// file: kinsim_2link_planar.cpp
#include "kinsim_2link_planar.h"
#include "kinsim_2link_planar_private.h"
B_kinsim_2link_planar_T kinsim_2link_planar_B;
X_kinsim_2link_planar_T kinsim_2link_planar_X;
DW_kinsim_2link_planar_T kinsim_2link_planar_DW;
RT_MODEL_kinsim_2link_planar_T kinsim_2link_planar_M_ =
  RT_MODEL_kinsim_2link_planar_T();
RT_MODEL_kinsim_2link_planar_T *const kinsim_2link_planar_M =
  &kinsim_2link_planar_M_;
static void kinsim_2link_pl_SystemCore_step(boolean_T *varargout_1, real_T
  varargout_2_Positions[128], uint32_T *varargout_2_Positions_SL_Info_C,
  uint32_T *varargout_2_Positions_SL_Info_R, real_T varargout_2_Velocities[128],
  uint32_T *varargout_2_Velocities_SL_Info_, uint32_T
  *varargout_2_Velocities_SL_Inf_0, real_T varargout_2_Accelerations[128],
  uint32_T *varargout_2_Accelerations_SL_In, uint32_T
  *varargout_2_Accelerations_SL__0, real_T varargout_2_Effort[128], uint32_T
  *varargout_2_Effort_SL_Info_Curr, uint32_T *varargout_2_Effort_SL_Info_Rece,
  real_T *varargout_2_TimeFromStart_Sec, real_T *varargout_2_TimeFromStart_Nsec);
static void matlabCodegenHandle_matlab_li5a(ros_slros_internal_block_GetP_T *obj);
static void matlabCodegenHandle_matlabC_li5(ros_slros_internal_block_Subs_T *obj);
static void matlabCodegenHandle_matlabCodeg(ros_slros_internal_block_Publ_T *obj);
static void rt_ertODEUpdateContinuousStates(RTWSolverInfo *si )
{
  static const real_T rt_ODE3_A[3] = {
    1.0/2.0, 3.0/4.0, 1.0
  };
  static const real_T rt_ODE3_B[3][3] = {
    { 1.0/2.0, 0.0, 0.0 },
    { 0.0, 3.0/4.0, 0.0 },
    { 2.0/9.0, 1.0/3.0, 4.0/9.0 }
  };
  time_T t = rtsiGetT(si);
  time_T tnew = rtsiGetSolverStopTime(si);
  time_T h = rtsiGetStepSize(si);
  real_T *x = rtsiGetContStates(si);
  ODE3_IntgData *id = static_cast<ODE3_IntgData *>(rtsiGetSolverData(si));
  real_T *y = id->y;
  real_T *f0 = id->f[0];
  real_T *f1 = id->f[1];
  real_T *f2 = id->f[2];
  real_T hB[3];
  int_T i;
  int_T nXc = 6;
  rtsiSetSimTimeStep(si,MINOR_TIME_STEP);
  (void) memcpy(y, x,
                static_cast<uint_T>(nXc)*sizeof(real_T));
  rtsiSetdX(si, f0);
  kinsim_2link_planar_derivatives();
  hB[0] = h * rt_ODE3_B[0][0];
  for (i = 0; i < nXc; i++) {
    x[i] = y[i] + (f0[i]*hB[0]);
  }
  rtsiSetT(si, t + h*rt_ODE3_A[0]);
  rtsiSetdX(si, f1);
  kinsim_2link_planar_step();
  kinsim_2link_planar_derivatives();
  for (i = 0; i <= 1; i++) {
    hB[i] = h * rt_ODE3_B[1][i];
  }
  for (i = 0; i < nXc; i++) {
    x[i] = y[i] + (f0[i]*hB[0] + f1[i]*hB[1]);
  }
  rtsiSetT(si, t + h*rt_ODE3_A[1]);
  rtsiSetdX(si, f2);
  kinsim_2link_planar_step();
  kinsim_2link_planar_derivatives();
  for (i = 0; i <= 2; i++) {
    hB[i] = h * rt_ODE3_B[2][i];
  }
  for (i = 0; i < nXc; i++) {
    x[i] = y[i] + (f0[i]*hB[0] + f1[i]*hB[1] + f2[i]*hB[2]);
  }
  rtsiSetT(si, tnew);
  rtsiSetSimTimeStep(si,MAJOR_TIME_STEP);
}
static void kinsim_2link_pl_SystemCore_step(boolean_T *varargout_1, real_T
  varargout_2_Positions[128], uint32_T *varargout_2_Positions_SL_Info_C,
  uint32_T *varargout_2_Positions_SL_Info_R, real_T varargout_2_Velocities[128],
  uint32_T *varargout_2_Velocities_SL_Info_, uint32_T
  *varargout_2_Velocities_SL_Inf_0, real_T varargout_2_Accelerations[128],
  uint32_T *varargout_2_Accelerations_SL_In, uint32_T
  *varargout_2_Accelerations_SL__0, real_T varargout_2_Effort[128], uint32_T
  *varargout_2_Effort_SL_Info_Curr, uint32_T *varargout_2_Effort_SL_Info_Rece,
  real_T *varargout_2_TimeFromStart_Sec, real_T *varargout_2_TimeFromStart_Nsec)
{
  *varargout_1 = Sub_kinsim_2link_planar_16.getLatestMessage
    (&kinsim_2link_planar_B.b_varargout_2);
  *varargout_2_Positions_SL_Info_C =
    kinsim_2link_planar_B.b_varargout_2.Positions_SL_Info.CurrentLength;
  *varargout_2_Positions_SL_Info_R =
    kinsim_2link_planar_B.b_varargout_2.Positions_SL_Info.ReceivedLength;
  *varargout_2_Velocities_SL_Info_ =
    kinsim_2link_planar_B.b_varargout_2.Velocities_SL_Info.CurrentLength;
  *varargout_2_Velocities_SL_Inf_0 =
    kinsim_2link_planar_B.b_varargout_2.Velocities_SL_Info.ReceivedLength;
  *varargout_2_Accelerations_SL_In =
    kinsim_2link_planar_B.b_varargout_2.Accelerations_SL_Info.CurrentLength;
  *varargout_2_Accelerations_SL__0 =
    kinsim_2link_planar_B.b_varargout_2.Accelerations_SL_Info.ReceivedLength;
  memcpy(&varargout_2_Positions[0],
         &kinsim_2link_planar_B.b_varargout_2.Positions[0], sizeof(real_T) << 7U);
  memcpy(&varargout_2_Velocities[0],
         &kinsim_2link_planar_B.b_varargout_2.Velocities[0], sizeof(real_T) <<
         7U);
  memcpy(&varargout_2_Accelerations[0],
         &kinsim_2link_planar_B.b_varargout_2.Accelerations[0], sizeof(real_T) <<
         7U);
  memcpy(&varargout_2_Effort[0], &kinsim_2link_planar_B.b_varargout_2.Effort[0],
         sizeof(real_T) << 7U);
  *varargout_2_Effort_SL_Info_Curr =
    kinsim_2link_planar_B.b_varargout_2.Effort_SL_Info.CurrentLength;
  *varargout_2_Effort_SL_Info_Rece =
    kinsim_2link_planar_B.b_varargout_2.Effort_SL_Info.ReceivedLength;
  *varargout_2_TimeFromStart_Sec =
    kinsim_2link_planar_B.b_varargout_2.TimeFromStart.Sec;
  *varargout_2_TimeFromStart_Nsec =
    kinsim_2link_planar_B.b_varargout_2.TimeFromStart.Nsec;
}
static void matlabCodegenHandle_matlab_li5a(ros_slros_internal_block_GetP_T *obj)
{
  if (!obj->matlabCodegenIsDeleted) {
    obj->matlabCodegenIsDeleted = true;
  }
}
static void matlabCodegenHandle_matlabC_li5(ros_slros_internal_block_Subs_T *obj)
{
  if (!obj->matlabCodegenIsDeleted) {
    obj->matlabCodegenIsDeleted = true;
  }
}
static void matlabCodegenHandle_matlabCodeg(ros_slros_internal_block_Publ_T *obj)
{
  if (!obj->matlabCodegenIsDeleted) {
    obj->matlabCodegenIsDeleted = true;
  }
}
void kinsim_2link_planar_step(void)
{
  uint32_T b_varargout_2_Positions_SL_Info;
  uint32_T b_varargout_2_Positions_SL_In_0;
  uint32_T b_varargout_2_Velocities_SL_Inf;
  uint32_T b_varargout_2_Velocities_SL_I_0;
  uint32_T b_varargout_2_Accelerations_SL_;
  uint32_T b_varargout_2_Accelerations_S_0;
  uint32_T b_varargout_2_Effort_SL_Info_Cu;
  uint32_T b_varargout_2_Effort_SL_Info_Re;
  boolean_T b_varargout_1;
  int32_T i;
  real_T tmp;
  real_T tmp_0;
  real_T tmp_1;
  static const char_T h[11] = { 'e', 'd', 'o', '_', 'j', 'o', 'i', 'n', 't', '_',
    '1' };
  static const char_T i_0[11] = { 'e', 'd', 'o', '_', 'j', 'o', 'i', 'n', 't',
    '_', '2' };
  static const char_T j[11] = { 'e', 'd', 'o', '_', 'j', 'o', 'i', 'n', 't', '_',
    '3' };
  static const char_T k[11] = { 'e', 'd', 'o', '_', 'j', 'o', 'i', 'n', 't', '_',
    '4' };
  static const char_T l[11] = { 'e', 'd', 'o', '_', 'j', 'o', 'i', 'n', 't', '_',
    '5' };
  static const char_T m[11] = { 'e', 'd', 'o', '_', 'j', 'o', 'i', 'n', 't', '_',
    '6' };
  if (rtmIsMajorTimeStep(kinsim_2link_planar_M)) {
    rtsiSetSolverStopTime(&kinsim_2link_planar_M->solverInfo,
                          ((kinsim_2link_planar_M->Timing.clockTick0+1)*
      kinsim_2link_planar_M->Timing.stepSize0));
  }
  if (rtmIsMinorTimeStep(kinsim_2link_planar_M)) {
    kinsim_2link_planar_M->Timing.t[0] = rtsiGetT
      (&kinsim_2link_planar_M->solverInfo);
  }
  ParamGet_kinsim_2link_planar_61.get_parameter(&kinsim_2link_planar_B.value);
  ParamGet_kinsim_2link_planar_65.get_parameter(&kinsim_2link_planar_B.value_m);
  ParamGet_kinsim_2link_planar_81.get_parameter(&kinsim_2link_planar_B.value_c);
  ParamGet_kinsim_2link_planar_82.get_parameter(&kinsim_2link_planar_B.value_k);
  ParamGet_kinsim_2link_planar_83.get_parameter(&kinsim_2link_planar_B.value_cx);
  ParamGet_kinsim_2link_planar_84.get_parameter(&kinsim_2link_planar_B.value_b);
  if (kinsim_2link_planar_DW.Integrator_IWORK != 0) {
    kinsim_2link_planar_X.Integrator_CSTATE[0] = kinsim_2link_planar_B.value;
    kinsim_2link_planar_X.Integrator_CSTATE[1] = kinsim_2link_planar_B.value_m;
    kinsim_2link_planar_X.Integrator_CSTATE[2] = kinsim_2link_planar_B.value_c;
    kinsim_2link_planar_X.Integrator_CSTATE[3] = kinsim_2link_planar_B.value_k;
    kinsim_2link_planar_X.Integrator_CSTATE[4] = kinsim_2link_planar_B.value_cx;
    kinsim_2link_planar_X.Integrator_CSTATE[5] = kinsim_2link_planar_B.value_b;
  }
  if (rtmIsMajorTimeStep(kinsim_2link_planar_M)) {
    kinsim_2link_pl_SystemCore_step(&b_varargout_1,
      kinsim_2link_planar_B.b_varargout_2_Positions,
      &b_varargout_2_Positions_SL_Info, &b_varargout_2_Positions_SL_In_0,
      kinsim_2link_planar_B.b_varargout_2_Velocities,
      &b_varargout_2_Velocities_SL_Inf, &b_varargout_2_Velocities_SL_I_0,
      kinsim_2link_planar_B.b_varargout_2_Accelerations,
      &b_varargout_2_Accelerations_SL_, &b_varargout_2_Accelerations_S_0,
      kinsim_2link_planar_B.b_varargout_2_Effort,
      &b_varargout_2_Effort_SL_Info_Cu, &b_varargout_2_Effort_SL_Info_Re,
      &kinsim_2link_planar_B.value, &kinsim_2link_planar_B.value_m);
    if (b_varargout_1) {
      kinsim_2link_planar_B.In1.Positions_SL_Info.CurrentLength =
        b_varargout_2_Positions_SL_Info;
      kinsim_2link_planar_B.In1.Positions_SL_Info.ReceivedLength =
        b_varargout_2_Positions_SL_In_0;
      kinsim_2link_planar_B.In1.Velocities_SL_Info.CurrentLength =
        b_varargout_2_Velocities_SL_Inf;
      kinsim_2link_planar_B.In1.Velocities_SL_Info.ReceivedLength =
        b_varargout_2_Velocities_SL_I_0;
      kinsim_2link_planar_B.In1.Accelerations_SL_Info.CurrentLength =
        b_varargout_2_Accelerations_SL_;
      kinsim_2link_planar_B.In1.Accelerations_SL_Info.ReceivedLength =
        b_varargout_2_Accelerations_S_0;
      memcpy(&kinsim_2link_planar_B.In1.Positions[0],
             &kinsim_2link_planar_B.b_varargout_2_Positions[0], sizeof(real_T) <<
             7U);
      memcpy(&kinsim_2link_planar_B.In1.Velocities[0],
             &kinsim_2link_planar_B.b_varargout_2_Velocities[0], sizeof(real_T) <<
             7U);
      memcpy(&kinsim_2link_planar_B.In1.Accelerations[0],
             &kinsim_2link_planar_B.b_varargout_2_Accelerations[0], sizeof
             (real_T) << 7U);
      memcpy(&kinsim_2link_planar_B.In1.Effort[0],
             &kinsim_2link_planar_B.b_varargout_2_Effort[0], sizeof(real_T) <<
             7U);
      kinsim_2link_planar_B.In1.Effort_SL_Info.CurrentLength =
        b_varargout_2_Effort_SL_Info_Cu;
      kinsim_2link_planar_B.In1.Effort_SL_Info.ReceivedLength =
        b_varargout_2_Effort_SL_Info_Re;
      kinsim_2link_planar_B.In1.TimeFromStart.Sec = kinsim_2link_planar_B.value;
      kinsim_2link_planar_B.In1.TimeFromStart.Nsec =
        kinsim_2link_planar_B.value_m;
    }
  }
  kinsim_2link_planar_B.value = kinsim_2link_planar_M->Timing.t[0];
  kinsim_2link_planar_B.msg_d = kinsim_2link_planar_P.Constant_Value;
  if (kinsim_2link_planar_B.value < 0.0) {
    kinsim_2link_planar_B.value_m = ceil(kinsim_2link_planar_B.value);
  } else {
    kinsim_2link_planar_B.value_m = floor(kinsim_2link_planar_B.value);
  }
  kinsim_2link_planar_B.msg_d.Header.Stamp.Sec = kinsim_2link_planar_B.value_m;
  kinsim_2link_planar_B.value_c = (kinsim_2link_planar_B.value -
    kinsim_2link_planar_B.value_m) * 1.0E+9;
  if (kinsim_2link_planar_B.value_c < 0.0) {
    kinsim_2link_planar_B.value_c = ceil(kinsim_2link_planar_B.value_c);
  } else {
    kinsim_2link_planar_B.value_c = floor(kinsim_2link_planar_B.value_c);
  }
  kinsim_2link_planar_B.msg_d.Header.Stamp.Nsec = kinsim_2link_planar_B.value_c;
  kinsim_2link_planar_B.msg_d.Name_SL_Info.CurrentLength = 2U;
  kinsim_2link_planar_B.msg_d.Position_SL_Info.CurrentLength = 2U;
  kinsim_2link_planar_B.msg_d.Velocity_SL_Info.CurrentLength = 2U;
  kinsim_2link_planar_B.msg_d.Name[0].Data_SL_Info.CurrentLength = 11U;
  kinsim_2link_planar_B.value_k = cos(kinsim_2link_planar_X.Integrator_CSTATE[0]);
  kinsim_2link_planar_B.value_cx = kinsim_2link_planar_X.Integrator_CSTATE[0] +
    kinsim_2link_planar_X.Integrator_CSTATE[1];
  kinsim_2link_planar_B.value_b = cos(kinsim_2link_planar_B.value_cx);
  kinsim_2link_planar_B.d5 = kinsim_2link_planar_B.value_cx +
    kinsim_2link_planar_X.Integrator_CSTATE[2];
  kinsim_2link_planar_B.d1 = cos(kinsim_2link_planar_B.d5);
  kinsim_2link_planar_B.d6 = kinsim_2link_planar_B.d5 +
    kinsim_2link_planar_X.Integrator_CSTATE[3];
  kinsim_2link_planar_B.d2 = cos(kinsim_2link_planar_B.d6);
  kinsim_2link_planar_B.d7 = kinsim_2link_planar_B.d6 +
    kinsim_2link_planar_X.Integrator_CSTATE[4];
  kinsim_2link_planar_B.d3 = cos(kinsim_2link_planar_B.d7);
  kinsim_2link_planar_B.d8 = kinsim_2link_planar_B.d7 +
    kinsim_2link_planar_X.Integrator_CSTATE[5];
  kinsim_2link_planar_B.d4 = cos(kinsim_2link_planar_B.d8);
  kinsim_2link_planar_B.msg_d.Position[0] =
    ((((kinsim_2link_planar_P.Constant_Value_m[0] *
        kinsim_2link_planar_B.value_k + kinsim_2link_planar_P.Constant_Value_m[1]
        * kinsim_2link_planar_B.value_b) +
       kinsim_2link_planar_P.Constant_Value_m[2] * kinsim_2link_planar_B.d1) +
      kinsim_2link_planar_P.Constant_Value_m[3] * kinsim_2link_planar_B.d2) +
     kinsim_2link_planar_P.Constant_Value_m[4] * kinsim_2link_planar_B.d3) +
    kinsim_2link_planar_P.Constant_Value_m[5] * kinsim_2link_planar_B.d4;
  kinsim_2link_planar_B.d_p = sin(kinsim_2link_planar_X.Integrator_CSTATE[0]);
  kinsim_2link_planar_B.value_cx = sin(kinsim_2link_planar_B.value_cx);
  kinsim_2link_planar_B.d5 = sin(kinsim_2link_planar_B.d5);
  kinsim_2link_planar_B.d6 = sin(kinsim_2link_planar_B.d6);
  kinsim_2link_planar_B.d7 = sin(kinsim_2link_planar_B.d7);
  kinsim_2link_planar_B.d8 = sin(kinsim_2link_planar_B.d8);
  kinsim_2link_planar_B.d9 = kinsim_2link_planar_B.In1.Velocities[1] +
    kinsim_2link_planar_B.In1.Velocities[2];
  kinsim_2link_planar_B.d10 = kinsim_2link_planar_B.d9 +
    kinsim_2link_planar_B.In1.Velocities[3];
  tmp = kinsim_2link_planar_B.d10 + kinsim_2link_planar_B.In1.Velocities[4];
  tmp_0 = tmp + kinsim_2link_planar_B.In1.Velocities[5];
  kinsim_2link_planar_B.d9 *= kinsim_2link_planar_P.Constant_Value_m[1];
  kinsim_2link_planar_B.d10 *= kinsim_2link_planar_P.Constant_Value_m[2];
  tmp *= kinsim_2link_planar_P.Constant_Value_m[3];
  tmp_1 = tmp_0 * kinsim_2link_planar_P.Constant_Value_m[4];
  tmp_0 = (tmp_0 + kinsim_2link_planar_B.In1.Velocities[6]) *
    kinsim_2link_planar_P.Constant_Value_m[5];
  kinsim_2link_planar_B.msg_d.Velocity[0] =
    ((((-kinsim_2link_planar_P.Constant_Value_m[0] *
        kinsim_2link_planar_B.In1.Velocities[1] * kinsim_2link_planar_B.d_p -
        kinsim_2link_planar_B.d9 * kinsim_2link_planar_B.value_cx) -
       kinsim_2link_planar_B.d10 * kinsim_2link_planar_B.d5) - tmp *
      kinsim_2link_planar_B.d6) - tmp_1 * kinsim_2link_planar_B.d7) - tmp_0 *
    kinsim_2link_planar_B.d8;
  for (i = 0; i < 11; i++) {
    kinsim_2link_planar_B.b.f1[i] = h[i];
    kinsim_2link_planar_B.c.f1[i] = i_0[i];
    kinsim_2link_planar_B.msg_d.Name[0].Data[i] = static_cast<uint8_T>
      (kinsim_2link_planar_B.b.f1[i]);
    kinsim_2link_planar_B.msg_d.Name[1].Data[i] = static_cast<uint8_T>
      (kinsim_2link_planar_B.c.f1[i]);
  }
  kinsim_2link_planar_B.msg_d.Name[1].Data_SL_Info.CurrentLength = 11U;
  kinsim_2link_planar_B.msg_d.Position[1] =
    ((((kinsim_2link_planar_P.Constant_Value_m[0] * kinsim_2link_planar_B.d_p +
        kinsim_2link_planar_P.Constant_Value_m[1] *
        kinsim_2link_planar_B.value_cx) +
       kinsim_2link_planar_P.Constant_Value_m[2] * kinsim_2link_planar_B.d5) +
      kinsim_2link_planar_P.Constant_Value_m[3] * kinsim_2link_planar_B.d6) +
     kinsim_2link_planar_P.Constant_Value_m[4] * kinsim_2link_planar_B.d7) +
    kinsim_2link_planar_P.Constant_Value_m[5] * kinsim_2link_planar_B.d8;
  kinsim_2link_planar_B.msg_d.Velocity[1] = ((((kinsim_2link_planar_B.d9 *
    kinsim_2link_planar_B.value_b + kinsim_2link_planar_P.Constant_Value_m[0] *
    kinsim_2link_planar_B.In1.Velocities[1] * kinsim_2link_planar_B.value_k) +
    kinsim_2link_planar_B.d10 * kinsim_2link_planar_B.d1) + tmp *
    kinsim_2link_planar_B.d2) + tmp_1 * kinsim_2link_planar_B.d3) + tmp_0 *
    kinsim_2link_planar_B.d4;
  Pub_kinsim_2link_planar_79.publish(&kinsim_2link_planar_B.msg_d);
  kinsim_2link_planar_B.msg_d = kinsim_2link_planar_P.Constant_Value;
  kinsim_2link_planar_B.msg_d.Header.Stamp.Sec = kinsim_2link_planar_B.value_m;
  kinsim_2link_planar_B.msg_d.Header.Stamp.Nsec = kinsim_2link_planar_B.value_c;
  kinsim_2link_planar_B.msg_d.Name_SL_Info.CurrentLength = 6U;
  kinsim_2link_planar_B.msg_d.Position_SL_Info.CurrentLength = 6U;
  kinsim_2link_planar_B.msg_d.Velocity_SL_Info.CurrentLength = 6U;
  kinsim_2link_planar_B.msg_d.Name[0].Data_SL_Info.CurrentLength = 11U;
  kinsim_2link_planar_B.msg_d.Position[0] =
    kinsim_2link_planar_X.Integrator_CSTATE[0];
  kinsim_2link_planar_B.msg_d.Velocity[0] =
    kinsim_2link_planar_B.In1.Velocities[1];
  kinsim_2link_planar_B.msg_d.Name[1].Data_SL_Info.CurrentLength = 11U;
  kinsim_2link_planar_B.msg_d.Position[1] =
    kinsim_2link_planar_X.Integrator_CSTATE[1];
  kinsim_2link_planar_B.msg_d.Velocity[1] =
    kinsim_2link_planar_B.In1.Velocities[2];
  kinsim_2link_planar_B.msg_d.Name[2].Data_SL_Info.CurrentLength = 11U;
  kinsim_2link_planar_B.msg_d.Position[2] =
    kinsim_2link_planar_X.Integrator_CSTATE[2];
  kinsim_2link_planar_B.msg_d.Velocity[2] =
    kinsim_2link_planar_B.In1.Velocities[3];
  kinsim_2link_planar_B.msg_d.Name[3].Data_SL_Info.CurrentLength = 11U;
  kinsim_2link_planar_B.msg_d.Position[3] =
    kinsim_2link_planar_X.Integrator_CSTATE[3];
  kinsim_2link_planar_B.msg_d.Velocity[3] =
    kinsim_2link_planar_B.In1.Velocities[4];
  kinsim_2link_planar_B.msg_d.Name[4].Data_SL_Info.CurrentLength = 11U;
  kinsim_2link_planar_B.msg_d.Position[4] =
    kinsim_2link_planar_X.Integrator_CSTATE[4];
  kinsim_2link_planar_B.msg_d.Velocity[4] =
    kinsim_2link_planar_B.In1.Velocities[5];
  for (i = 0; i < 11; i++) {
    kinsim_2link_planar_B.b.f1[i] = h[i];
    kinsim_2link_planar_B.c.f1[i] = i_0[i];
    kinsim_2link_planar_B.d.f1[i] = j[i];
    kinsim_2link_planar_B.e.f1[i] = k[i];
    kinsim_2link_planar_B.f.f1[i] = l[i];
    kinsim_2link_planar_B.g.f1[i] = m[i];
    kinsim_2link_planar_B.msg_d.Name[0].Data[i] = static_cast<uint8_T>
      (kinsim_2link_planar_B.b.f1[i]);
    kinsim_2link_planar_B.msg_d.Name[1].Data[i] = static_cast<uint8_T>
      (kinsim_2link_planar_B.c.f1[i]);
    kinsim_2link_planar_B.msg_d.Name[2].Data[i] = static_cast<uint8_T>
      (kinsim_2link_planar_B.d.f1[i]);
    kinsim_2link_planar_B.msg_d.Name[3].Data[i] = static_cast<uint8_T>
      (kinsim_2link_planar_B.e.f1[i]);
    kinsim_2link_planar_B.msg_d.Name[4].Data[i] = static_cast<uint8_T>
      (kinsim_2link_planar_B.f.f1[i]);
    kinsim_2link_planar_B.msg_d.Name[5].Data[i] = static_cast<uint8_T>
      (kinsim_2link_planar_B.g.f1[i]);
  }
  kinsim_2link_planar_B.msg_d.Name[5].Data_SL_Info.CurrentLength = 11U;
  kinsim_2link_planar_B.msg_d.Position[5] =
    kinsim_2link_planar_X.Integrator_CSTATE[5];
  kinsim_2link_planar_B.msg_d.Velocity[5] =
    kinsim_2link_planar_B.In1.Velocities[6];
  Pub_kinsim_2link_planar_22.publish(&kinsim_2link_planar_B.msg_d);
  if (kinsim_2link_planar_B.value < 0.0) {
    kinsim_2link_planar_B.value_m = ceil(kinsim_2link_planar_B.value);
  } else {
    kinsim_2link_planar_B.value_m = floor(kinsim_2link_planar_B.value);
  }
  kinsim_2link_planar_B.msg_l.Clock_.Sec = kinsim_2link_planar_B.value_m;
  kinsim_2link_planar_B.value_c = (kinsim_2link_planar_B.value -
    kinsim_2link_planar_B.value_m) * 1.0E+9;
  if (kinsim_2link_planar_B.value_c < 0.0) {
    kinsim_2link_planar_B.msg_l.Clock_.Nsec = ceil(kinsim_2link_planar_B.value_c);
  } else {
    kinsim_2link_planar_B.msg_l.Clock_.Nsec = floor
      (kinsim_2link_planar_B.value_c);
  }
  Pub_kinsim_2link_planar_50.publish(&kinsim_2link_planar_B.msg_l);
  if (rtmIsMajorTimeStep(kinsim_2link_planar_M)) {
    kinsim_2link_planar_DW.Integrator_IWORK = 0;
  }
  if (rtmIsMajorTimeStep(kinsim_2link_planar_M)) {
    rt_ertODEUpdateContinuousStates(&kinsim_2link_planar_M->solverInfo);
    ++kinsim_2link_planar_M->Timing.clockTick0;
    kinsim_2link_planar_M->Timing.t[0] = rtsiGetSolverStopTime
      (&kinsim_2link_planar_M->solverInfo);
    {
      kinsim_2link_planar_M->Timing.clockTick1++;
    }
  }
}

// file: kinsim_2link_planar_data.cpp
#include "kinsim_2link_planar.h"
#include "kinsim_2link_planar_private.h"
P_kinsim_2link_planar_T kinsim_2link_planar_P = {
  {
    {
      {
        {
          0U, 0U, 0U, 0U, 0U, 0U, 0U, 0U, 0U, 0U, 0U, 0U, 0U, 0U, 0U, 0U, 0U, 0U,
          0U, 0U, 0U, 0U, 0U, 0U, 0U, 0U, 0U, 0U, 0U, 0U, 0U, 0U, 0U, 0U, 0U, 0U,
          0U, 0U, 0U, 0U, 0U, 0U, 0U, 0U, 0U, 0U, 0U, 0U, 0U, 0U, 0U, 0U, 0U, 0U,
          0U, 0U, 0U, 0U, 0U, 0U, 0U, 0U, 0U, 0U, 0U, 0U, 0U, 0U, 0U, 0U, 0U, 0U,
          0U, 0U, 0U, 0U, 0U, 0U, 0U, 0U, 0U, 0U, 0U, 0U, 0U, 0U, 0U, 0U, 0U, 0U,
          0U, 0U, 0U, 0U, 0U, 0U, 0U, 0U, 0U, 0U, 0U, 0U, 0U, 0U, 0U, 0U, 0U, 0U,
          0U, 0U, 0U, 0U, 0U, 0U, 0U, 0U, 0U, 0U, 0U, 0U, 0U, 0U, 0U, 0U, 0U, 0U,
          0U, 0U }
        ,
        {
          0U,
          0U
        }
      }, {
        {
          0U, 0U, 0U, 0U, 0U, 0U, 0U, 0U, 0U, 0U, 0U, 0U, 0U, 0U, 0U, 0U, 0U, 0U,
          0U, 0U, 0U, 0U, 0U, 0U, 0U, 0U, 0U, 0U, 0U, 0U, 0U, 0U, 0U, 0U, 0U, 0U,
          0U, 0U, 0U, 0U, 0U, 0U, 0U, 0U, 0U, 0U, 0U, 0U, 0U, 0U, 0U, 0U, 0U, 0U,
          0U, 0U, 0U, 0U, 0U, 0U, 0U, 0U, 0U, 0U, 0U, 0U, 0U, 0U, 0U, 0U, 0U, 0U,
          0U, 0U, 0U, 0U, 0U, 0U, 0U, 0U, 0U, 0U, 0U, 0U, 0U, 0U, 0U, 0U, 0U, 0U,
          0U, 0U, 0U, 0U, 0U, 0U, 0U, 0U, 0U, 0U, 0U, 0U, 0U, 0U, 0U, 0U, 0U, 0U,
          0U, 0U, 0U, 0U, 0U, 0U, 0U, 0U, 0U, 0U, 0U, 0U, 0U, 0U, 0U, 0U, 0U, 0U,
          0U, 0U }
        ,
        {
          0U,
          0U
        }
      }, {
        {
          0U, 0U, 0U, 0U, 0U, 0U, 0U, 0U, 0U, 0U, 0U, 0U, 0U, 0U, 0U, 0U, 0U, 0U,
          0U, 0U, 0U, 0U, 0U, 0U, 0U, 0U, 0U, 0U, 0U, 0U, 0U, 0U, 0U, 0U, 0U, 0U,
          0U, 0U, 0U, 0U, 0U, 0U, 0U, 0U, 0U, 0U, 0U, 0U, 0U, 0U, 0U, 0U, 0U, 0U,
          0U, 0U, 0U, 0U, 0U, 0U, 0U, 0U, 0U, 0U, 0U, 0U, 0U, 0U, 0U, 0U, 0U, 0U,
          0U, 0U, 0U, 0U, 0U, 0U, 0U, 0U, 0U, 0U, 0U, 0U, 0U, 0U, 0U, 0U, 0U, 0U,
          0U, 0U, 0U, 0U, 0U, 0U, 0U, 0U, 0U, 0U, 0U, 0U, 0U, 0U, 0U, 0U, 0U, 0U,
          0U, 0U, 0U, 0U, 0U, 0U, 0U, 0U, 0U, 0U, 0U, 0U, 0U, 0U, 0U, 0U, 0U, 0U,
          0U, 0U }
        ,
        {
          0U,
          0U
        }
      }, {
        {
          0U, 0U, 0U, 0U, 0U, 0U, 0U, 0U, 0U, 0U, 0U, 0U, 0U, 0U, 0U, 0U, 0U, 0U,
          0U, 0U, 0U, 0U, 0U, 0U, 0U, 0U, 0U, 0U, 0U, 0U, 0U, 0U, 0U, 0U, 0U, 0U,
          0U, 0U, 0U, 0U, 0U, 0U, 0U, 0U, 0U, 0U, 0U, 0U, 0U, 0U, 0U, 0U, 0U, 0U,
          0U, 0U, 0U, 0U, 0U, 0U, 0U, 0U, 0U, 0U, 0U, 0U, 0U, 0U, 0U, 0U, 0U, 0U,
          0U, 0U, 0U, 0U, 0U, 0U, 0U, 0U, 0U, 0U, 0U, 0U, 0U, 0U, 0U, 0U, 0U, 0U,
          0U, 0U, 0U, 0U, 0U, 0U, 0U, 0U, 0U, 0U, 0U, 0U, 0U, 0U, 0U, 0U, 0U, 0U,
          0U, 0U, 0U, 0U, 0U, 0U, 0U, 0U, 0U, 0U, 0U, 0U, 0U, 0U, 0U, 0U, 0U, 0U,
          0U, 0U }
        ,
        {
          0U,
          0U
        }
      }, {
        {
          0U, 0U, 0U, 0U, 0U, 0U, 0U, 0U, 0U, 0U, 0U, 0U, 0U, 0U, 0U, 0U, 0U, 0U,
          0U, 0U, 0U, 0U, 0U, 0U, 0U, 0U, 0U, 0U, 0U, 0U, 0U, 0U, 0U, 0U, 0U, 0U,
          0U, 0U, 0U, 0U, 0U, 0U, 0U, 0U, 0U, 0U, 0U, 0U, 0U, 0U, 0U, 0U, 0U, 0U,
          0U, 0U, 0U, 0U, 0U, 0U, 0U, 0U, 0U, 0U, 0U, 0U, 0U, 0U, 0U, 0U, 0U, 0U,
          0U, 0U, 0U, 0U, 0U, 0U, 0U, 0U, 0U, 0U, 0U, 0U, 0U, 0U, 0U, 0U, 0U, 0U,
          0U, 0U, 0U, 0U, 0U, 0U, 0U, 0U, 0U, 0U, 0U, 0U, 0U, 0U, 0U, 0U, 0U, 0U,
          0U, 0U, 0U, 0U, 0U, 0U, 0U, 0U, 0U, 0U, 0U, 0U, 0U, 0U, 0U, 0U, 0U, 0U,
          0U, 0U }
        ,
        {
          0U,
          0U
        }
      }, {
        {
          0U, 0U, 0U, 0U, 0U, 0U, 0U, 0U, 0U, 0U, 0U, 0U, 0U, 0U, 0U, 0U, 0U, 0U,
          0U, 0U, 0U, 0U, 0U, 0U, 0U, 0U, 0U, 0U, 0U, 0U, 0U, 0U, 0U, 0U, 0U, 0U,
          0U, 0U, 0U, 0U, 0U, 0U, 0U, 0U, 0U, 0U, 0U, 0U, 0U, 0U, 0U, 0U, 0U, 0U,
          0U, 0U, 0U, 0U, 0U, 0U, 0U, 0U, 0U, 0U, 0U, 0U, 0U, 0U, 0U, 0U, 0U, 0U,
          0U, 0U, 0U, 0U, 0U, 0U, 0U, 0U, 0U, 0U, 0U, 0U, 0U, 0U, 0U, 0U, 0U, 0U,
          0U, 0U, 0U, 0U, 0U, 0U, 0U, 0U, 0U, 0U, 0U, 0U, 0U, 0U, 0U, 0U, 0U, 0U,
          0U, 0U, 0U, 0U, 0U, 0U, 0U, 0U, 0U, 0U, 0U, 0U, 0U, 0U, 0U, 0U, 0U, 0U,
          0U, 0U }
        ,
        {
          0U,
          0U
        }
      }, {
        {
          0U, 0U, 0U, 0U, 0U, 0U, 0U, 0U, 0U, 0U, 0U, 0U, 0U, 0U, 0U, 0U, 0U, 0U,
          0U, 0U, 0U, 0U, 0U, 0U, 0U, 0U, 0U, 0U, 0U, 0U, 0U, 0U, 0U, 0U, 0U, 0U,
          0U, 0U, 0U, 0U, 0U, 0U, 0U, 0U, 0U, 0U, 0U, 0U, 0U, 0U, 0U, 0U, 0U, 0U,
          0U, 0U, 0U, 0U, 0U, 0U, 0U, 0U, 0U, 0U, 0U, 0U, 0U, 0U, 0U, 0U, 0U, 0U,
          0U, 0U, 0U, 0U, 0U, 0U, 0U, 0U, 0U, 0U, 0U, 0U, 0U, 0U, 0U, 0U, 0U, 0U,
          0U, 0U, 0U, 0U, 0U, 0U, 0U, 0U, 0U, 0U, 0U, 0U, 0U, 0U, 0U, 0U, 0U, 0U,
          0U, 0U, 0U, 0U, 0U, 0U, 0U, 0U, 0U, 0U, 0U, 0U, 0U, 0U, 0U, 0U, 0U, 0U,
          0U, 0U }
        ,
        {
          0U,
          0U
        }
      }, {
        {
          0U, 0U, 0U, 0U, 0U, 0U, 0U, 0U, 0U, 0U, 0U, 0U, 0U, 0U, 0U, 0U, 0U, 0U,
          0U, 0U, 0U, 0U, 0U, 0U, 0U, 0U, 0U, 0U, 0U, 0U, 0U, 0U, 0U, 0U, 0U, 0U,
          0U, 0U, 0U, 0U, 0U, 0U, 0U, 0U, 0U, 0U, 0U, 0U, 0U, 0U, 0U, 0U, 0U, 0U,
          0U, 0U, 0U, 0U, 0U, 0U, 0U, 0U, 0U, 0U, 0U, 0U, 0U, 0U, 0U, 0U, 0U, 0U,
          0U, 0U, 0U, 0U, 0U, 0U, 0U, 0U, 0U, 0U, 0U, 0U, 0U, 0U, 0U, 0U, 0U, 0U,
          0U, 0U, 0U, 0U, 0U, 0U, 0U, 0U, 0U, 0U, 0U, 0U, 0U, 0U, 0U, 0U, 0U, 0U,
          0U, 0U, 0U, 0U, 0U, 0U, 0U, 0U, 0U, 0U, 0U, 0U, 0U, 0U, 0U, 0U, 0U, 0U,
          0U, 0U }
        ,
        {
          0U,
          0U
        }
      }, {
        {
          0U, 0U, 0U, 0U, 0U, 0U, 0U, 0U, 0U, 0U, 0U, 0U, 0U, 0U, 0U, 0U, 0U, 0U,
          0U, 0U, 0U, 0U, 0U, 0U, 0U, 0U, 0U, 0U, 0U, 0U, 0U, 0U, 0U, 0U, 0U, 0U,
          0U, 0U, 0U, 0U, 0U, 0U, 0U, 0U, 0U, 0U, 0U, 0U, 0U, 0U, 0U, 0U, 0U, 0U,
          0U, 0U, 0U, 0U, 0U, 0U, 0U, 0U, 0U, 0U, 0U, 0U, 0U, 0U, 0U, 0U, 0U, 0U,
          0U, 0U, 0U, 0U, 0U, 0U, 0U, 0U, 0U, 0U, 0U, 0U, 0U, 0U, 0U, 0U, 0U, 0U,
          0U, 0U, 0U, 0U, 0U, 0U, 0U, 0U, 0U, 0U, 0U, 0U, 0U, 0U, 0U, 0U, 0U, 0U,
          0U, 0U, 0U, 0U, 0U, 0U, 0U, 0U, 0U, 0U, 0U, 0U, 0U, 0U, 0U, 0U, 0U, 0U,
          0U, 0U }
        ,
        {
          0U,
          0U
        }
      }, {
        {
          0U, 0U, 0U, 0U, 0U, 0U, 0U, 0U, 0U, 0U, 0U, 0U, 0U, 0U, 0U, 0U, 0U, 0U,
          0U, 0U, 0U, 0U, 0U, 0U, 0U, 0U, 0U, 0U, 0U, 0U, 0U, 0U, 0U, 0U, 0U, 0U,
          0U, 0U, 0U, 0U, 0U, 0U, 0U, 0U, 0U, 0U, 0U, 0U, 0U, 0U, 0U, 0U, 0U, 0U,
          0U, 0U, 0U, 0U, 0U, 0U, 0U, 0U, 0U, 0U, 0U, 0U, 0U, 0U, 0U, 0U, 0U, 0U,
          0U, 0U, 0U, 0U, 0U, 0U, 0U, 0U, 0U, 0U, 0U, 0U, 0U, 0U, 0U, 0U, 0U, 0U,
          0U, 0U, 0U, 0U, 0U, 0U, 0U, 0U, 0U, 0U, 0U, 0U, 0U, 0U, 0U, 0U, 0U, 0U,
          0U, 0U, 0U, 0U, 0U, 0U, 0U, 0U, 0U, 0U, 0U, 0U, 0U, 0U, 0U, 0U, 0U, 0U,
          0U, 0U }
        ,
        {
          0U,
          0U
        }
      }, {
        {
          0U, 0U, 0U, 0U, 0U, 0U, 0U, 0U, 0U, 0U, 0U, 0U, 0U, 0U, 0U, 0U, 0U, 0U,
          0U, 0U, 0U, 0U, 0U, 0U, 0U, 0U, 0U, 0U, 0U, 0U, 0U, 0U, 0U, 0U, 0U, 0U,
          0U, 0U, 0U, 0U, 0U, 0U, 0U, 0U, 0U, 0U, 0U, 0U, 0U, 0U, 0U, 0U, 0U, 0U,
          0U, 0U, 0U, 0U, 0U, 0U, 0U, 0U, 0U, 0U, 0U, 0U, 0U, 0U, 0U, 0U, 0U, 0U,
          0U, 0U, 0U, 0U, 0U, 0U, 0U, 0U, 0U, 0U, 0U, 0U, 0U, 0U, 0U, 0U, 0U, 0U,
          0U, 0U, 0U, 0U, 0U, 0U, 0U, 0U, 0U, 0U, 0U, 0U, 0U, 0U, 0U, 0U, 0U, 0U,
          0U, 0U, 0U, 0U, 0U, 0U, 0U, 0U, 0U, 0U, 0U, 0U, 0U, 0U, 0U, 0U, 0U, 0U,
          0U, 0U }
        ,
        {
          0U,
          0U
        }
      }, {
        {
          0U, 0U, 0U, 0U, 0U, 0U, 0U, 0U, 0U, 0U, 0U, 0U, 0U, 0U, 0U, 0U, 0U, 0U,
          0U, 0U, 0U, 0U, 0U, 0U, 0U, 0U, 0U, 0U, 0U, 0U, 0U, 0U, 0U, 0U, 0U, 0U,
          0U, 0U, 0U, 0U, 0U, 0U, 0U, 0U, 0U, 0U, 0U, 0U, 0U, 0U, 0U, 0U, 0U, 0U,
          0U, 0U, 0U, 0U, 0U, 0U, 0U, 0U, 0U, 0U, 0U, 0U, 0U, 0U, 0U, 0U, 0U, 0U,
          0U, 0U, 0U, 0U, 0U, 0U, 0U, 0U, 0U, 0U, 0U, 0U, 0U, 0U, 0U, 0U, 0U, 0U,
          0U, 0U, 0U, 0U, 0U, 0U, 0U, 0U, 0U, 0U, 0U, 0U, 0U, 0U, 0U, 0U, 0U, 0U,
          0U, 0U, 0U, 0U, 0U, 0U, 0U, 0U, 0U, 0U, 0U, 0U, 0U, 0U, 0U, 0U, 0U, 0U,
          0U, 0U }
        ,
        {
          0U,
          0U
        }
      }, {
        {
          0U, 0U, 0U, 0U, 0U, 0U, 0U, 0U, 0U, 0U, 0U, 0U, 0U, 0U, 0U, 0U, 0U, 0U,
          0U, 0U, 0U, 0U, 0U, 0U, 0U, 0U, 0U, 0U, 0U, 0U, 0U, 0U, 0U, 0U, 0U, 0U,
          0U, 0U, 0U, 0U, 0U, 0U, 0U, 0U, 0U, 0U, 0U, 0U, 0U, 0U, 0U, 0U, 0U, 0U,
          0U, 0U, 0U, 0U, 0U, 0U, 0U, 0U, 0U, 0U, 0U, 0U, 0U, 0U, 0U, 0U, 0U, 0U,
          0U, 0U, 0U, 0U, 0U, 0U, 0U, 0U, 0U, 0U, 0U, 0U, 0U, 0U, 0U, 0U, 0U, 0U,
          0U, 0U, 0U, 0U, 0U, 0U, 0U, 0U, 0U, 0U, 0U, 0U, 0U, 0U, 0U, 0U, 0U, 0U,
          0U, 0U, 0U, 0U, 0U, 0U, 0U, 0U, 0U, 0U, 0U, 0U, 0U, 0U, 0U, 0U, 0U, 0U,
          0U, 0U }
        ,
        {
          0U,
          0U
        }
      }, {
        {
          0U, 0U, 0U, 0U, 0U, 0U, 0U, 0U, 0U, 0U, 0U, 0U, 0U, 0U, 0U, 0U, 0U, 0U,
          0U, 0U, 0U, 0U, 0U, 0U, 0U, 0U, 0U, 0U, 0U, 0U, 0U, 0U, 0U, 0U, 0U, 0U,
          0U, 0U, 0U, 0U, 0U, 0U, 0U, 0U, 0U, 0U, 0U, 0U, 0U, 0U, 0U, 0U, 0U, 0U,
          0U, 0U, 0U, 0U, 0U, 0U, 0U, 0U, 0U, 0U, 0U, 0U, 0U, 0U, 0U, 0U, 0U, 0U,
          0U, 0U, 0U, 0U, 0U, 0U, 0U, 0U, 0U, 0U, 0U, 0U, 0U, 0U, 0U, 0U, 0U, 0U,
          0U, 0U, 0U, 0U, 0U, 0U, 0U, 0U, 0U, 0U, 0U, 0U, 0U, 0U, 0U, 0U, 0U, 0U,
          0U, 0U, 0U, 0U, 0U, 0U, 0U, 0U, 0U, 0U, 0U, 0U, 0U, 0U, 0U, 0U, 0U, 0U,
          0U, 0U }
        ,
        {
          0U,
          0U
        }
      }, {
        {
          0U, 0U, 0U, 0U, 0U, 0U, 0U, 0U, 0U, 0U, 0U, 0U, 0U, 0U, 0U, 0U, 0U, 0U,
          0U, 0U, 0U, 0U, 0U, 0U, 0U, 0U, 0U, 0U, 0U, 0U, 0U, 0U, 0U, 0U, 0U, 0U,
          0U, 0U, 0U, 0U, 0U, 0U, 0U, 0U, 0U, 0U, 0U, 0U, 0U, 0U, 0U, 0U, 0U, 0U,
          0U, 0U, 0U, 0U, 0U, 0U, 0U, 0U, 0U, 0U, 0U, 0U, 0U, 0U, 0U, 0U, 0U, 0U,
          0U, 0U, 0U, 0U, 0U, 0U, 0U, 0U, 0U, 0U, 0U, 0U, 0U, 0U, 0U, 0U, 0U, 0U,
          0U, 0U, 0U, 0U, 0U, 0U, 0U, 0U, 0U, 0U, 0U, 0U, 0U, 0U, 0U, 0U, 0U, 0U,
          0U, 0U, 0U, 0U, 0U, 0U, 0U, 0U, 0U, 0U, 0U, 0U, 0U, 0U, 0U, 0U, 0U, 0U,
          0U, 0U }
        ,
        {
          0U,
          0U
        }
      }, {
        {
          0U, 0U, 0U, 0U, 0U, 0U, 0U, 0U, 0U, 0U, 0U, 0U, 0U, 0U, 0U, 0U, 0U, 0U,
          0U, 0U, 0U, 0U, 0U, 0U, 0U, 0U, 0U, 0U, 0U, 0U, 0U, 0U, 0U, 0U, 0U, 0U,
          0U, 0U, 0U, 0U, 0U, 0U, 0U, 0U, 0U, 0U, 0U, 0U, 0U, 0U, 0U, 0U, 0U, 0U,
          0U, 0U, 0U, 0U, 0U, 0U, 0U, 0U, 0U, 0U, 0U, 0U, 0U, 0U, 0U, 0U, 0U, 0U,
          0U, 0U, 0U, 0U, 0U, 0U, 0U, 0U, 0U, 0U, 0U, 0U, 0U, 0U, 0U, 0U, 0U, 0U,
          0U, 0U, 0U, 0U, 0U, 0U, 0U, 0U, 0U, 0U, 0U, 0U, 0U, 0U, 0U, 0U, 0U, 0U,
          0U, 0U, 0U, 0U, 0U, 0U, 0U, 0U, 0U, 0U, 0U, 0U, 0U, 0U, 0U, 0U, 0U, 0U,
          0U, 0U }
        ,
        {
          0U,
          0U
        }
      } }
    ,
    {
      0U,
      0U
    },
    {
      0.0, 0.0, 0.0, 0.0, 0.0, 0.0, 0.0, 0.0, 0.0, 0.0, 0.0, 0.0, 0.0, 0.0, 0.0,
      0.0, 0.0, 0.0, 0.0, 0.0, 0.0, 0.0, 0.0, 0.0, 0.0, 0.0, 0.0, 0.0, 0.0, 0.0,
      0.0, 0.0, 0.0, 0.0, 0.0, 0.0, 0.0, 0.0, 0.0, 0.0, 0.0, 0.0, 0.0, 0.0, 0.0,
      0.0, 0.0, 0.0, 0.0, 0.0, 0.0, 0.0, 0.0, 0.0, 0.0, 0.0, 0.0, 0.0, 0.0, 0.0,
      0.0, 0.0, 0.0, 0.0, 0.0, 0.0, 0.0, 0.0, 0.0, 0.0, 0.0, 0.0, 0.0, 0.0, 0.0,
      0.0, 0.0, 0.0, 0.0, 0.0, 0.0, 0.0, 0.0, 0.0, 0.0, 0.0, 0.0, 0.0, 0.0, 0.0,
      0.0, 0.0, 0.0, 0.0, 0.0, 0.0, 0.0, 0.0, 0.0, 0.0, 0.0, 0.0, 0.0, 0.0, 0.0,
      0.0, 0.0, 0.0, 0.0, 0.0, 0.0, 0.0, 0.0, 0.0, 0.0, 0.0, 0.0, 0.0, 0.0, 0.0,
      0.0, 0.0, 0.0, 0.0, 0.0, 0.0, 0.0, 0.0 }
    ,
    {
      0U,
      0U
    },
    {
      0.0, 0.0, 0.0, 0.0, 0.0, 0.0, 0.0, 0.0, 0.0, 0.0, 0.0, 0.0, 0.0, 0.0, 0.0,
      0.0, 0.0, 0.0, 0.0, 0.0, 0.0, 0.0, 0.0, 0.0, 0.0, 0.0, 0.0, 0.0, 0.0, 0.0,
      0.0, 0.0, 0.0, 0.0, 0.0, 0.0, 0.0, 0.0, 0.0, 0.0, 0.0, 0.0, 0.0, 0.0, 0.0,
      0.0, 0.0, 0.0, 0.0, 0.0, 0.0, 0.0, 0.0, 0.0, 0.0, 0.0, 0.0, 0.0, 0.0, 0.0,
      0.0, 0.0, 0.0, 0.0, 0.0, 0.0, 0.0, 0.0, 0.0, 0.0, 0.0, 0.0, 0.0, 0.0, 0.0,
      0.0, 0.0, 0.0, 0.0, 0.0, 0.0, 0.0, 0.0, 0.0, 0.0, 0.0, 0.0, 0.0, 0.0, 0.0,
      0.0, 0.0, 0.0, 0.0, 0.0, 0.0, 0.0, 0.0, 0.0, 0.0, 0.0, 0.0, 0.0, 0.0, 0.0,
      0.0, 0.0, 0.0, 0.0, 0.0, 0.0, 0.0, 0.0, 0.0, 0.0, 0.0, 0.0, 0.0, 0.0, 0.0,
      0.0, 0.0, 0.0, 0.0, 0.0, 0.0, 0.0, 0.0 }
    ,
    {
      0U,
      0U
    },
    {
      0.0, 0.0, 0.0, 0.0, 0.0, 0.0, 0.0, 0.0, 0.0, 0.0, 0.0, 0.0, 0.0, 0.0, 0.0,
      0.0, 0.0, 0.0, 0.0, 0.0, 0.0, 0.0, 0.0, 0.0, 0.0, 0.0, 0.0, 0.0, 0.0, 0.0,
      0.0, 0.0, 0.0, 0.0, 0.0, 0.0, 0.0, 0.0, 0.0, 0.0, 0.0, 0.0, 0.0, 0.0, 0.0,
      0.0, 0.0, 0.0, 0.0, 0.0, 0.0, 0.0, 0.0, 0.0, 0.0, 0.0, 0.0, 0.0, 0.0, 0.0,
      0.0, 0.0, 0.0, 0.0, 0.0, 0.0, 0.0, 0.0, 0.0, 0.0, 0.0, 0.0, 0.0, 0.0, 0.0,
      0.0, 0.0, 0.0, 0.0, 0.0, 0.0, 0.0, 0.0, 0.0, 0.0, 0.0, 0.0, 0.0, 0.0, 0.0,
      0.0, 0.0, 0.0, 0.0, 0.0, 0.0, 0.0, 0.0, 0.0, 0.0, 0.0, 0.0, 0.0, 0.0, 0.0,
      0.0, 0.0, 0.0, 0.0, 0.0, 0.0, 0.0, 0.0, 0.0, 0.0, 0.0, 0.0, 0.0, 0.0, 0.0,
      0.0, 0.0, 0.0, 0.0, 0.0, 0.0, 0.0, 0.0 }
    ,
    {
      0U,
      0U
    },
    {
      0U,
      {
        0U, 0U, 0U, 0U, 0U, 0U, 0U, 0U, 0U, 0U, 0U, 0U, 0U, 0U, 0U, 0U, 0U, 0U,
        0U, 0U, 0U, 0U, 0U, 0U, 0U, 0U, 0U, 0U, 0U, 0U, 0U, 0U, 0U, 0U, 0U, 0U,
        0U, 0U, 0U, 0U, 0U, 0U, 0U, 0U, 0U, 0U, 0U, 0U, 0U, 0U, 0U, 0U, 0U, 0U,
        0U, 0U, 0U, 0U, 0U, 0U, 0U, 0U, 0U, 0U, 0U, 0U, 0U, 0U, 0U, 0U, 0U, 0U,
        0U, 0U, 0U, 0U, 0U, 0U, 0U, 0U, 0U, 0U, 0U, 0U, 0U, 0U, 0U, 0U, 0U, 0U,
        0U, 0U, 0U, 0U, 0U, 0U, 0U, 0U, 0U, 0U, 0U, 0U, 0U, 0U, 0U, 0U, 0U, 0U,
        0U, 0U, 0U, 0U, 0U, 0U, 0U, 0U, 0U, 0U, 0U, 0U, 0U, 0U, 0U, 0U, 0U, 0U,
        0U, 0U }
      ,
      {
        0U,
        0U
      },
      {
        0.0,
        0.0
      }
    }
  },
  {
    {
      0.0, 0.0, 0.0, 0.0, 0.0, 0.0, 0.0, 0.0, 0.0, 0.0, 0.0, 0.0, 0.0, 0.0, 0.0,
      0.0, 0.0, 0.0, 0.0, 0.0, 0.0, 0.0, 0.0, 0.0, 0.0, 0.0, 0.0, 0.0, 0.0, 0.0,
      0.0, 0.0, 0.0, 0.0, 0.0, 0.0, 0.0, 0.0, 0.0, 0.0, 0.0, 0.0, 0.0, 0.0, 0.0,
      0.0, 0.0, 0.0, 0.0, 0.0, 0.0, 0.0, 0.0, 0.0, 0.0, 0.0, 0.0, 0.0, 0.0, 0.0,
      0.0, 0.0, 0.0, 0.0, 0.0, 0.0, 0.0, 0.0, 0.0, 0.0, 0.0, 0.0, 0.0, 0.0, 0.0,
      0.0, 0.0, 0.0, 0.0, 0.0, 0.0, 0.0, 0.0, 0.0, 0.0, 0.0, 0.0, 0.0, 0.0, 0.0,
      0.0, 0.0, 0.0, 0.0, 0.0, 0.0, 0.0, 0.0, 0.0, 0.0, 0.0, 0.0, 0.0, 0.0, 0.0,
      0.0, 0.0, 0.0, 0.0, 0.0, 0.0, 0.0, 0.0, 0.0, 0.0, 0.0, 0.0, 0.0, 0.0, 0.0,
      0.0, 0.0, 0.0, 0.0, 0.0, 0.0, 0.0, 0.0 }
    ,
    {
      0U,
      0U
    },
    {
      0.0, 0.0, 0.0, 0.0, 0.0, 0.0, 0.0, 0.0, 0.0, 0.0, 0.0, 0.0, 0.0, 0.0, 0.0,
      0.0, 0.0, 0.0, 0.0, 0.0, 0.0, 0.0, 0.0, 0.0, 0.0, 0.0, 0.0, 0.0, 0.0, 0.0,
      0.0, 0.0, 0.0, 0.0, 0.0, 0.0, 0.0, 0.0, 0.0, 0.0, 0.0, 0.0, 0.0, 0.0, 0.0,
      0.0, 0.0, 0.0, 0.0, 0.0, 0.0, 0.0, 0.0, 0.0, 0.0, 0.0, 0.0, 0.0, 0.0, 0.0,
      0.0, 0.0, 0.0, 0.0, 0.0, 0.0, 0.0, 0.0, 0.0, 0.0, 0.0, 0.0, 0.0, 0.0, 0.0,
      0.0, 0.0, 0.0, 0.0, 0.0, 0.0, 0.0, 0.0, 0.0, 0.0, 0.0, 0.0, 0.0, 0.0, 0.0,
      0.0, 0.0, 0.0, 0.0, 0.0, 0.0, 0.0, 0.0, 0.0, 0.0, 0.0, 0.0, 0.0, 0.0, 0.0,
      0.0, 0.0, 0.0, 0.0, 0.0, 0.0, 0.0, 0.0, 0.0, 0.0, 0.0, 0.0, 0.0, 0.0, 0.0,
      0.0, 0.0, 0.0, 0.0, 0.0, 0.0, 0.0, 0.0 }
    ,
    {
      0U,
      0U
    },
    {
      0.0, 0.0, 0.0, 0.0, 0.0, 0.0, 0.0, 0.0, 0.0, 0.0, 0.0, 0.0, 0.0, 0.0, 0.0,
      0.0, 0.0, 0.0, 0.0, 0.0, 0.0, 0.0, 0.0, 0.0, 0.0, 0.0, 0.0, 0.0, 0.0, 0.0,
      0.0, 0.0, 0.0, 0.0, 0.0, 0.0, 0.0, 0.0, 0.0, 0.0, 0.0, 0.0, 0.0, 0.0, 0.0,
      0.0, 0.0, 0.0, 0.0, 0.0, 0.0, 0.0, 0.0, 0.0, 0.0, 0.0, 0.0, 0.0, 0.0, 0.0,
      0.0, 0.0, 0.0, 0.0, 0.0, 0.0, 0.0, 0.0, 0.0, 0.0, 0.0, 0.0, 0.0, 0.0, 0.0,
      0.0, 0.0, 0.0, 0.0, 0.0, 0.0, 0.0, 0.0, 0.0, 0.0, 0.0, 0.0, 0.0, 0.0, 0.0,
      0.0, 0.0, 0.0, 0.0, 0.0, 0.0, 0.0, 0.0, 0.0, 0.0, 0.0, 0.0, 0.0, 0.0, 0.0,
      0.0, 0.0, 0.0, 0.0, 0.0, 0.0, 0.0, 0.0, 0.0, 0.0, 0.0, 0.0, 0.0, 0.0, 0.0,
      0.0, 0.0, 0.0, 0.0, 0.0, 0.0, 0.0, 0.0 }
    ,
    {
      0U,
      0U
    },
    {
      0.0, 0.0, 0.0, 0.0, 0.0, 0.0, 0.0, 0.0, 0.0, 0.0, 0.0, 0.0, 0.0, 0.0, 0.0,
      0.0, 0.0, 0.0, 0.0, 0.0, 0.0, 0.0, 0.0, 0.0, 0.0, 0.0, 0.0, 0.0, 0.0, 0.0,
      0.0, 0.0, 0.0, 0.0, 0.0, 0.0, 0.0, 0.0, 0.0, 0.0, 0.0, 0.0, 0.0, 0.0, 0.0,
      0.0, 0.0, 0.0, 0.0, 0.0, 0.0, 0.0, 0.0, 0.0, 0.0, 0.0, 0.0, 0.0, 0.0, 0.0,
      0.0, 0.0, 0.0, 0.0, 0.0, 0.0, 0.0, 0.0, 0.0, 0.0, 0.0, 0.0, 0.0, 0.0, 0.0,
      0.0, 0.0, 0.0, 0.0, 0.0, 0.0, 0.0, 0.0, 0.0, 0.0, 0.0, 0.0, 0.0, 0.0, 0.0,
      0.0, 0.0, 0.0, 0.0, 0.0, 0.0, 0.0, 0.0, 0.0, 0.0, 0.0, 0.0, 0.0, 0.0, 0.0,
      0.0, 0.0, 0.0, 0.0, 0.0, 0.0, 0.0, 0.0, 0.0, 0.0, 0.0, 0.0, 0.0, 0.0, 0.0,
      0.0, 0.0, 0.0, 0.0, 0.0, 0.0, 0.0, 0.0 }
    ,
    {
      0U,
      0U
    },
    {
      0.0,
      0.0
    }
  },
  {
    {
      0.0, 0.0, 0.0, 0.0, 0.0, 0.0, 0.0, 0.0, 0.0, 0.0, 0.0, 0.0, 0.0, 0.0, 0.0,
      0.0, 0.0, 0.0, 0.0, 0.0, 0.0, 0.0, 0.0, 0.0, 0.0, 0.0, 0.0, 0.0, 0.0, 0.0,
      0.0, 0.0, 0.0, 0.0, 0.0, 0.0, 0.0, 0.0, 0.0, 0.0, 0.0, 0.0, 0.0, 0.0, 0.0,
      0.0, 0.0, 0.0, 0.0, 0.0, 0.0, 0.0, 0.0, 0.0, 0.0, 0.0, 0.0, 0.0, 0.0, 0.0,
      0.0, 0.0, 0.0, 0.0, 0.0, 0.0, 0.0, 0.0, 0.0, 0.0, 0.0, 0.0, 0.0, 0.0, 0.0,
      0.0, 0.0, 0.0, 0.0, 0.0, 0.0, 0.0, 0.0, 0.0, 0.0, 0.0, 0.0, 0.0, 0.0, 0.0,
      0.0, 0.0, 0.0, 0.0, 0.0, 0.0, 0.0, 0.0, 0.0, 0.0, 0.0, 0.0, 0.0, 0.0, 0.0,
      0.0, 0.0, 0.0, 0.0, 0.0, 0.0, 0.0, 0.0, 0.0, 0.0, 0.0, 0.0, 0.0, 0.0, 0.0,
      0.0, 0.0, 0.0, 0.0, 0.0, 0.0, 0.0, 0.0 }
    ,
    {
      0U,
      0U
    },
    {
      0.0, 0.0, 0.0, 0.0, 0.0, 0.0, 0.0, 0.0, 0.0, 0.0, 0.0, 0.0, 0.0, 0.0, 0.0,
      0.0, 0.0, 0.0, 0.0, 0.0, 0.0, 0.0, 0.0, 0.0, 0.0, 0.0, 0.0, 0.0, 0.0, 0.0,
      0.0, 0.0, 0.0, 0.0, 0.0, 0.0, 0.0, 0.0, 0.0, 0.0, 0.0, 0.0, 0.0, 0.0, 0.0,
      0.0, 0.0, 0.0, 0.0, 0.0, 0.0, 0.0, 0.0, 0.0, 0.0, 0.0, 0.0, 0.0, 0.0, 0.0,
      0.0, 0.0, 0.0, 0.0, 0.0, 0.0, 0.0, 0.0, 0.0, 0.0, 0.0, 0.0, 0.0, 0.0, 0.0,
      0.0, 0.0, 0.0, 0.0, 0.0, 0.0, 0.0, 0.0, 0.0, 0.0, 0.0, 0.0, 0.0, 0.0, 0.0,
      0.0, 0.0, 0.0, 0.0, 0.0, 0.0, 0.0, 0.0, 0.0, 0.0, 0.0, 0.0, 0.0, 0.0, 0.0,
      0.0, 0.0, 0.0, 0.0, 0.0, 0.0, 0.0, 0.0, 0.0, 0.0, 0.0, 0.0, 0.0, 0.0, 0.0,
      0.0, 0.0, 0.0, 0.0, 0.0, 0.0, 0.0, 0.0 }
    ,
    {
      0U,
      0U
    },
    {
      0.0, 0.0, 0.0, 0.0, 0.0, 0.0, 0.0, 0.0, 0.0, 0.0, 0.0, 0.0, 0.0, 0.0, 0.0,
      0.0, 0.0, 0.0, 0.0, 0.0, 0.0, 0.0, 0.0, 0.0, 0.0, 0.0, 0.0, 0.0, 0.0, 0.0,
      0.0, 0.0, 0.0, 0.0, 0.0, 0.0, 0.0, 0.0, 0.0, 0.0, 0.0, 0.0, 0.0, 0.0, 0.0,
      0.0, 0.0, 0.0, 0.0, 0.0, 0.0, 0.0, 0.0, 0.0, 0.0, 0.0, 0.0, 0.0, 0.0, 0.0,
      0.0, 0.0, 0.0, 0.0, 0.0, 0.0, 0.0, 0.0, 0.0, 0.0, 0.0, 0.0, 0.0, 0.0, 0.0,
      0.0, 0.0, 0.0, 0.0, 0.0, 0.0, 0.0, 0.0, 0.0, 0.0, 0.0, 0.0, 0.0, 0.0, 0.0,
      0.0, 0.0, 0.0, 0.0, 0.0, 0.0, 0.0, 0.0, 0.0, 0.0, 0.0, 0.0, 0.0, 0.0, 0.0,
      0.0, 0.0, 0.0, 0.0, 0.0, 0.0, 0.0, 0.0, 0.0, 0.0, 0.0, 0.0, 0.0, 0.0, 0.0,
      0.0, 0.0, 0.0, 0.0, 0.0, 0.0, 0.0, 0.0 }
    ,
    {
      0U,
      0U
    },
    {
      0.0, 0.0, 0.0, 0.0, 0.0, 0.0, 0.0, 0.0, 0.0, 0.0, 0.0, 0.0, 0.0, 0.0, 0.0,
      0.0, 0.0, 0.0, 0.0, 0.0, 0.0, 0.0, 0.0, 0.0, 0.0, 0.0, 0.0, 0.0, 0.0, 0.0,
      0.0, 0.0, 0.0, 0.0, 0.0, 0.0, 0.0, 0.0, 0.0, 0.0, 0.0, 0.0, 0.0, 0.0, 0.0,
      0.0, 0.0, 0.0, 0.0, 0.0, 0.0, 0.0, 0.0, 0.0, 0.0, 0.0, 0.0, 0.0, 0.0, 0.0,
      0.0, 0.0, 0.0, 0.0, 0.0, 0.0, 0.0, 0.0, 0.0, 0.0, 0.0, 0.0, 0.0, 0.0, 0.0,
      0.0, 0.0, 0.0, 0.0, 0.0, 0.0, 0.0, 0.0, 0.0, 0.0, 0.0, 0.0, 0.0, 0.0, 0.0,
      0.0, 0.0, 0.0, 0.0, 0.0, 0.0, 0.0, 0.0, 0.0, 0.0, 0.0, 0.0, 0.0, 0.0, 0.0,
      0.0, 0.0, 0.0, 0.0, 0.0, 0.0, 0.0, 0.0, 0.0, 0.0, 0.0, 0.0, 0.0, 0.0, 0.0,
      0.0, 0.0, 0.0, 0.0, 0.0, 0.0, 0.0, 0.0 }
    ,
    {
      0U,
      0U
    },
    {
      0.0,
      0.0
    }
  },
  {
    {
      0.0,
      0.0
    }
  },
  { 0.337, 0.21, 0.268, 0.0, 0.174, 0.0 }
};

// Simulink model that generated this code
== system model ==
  Publish#1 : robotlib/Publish  <- 1: MATLABFunction#1
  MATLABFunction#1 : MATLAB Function  <- 1: BlankMessage#1, 2: MATLABFunction#2, 3: MATLABFunction#2/2, 4: Clock#1
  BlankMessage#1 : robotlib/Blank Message
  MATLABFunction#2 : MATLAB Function  <- 1: Integrator, 2: Selector#1, 3: Constant
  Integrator : Integrator  InitialCondition=[0,0]  <- 1: Selector#1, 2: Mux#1
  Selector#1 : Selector  Indices=[2]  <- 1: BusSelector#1
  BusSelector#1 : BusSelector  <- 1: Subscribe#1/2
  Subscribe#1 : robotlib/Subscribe
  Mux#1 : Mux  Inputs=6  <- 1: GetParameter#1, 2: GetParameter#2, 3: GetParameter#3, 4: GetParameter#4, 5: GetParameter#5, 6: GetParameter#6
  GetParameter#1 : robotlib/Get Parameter
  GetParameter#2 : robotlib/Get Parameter
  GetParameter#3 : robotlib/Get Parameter
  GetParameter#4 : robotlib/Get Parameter
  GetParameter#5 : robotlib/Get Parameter
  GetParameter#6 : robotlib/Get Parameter
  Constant : Constant  Value=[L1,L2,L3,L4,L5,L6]
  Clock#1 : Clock
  Publish#2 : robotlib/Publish  <- 1: MATLABFunction#3
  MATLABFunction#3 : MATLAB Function  <- 1: BlankMessage#1, 2: Integrator, 3: Selector#1, 4: Clock#1
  Publish#3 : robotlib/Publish  <- 1: MATLABFunction#4
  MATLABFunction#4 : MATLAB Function  <- 1: BlankMessage#2, 2: Clock
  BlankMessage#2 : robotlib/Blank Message
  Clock : Clock
== matlab function MATLABFunction#4 ==
function msg = assign_Time(blankMessage,time)
%#codegen

% Assign the output message to be the same with input blank message
msg = blankMessage;

% Convert and set time
msg.Clock_.Sec  = fix(time);
msg.Clock_.Nsec = fix((time-fix(time))*1e9);

== matlab function MATLABFunction#3 ==
function msg = assign_JointState(blankMessage,jointPos,jointVel,time)
%#codegen

% Assign the output message to be the same with input blank message
msg = blankMessage;

% Initialize time stamp
msg.Header.Stamp.Sec  = fix(time);
msg.Header.Stamp.Nsec = fix((time-fix(time))*1e9);

% Set the number of strings in the string array, and joint positions/velocities in the position/velocity array
numJoints = length(jointPos);
msg.Name_SL_Info.CurrentLength = uint32(numJoints);
msg.Position_SL_Info.CurrentLength = uint32(numJoints);
msg.Velocity_SL_Info.CurrentLength = uint32(numJoints);

% Set the individual components in the message arrays
strArrayToAssign = {'edo_joint_1', 'edo_joint_2', 'edo_joint_3', 'edo_joint_4', 'edo_joint_5', 'edo_joint_6'};

for idx=1:numJoints
    str = strArrayToAssign{idx};
    strLength = length(str);
    msg.Name(idx).Data(1:strLength) = uint8(str);
    msg.Name(idx).Data_SL_Info.CurrentLength = uint32(strLength);

    msg.Position(idx) = jointPos(idx);
    msg.Velocity(idx) = jointVel(idx);
end

== matlab function MATLABFunction#2 ==
function [cartPos, cartVel] = forward_kinematics_2link(jointPos,jointVel,linkLength)

cartPos = zeros(1,2);
cartVel = zeros(1,2);

L1 = linkLength(1);
L2 = linkLength(2);
L3 = linkLength(3);
L4 = linkLength(4);
L5 = linkLength(5);
L6 = linkLength(6);
q1 = jointPos(1);
q2 = jointPos(2);
q3 = jointPos(3);
q4 = jointPos(4);
q5 = jointPos(5);
q6 = jointPos(6);
qv1 = jointVel(1);
qv2 = jointVel(2);
qv3 = jointVel(3);
qv4 = jointVel(4);
qv5 = jointVel(5);
qv6 = jointVel(6);

cartPos(1) = L1*cos(q1)+L2*cos(q1+q2)+L3*cos(q1+q2+q3)+L4*cos(q1+q2+q3+q4)+L5*cos(q1+q2+q3+q4+q5)+L6*cos(q1+q2+q3+q4+q5+q6);
cartPos(2) = L1*sin(q1)+L2*sin(q1+q2)+L3*sin(q1+q2+q3)+L4*sin(q1+q2+q3+q4)+L5*sin(q1+q2+q3+q4+q5)+L6*sin(q1+q2+q3+q4+q5+q6);
cartVel(1) = -L1*qv1*sin(q1)-L2*(qv1+qv2)*sin(q1+q2)-L3*(qv1+qv2+qv3)*sin(q1+q2+q3)-L4*(qv1+qv2+qv3+qv4)*sin(q1+q2+q3+q4)-L5*(qv1+qv2+qv3+qv4+qv5)*sin(q1+q2+q3+q4+q5)-L6*(qv1+qv2+qv3+qv4+qv5+qv6)*sin(q1+q2+q3+q4+q5+q6);
cartVel(2) = L1*qv1*cos(q1)+L2*(qv1+qv2)*cos(q1+q2)+L3*(qv1+qv2+qv3)*cos(q1+q2+q3)+L4*(qv1+qv2+qv3+qv4)*cos(q1+q2+q3+q4)+L5*(qv1+qv2+qv3+qv4+qv5)*cos(q1+q2+q3+q4+q5)+L6*(qv1+qv2+qv3+qv4+qv5+qv6)*cos(q1+q2+q3+q4+q5+q6);

== matlab function MATLABFunction#1 ==
function msg = assign_CartesianState(blankMessage,cartPos,cartVel,time)
%#codegen

% Assign the output message to be the same with input blank message
msg = blankMessage;

% Initialize time stamp
msg.Header.Stamp.Sec  = fix(time);
msg.Header.Stamp.Nsec = fix((time-fix(time))*1e9);

% Set the number of strings in the string array, and joint positions/velocities in the position/velocity array
numCoordinates = length(cartPos);
msg.Name_SL_Info.CurrentLength = uint32(numCoordinates);
msg.Position_SL_Info.CurrentLength = uint32(numCoordinates);
msg.Velocity_SL_Info.CurrentLength = uint32(numCoordinates);

% Set the individual components in the message arrays
strArrayToAssign = {'edo_joint_1', 'edo_joint_2', 'edo_joint_3', 'edo_joint_4', 'edo_joint_5', 'edo_joint_6'};

for idx=1:numCoordinates
    str = strArrayToAssign{idx};
    strLength = length(str);
    msg.Name(idx).Data(1:strLength) = uint8(str);
    msg.Name(idx).Data_SL_Info.CurrentLength = uint32(strLength);

    msg.Position(idx) = cartPos(idx);
    msg.Velocity(idx) = cartVel(idx);
end
